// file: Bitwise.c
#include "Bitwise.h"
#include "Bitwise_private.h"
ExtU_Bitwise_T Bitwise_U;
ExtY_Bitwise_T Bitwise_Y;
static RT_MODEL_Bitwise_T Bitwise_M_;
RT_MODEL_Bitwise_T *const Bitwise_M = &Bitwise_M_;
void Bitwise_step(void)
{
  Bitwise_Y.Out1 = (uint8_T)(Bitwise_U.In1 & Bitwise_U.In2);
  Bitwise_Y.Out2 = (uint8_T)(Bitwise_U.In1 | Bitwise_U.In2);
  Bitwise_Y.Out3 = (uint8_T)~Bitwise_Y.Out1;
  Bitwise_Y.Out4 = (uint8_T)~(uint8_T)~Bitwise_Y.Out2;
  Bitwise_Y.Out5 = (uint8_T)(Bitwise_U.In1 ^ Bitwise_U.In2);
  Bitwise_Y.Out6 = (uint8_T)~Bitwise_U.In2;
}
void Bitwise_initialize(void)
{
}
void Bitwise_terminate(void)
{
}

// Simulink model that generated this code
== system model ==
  In1 : Inport
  In2 : Inport
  Out1 : Outport  <- 1: BitwiseOperator#1
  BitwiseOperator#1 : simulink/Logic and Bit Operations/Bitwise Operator  logicop=AND  BitMask=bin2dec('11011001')  <- 1: In1, 2: In2
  Out2 : Outport  <- 1: BitwiseOperator#2
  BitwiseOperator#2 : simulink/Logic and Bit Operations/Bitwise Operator  logicop=OR  BitMask=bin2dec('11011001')  <- 1: In1, 2: In2
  Out3 : Outport  <- 1: BitwiseOperator#3
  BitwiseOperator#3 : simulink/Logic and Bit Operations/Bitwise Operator  logicop=NAND  BitMask=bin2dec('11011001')  <- 1: In1, 2: In2
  Out4 : Outport  <- 1: BitwiseOperator#4
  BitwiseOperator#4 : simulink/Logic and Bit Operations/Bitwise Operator  logicop=NOT  BitMask=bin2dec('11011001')  <- 1: BitwiseOperator#5
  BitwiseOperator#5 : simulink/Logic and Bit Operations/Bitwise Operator  logicop=NOR  BitMask=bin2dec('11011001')  <- 1: In1, 2: In2
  Out5 : Outport  <- 1: BitwiseOperator#6
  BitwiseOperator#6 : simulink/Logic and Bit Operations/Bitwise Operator  logicop=XOR  BitMask=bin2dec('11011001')  <- 1: In1, 2: In2
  Out6 : Outport  <- 1: BitwiseOperator#7
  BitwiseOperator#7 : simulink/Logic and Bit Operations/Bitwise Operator  logicop=NOT  BitMask=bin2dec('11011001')  <- 1: In2
